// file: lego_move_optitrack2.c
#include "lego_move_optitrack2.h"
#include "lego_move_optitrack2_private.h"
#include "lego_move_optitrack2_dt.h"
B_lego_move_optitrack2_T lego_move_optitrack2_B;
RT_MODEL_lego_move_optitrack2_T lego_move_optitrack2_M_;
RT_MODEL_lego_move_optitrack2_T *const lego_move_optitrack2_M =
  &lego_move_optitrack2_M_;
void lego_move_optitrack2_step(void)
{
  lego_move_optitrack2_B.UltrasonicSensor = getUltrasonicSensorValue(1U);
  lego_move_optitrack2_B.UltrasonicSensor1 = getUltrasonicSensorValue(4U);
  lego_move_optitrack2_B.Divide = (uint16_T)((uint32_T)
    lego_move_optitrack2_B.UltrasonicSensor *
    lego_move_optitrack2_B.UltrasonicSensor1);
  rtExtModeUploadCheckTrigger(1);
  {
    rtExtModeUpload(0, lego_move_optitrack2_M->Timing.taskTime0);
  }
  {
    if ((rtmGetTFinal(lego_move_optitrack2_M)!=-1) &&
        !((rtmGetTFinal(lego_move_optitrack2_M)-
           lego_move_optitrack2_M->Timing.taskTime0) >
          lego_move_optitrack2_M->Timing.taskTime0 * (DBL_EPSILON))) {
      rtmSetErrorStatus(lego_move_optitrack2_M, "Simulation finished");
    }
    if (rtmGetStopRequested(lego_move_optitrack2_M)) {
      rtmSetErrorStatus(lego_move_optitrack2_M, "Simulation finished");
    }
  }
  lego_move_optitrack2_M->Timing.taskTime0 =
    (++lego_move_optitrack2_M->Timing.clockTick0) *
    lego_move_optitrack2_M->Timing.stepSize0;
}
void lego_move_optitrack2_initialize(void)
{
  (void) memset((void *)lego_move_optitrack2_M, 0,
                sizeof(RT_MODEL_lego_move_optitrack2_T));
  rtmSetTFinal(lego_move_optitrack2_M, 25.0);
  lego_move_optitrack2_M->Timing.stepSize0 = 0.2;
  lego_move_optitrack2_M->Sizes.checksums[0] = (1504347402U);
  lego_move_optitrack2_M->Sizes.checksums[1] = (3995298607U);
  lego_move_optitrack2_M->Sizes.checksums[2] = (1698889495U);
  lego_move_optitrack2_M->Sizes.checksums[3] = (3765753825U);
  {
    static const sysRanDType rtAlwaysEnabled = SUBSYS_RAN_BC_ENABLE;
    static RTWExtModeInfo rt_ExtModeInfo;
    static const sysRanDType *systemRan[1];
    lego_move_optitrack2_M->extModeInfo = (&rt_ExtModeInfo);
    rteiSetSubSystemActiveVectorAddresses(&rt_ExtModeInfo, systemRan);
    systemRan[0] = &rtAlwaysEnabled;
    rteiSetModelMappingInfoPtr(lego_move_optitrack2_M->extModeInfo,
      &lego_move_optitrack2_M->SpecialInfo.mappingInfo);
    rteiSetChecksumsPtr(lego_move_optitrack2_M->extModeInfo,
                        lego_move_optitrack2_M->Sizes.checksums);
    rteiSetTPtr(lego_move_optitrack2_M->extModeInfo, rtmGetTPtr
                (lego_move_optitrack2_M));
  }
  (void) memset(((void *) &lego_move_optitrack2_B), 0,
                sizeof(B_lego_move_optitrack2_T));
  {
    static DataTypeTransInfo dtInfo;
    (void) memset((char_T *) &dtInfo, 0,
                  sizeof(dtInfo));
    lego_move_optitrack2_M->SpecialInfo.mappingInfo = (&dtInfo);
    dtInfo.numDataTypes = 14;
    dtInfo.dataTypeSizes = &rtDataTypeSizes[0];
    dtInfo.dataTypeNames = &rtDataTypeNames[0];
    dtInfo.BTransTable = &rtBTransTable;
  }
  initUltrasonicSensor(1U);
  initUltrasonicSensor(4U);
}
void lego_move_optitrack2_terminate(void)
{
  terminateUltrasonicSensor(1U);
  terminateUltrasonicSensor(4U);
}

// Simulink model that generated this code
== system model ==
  Divide : Product  <- 1: UltrasonicSensor, 2: UltrasonicSensor1
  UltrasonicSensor : legoev3lib/Ultrasonic Sensor
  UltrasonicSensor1 : legoev3lib/Ultrasonic Sensor
